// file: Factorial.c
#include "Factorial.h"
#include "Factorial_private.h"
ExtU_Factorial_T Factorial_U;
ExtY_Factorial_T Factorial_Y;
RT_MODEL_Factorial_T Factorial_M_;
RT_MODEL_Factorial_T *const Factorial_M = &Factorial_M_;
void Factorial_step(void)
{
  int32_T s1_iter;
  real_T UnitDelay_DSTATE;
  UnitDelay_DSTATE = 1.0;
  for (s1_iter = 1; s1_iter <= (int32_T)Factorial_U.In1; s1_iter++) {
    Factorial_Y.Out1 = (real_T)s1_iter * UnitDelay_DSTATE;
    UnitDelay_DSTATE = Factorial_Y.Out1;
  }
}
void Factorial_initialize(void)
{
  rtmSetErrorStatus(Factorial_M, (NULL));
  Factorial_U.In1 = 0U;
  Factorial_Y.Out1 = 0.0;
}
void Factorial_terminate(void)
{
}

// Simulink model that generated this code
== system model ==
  In1 : Inport
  Out1 : Outport  <- 1: Subsystem#1
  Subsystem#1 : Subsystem  <- 1: In1
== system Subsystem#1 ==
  Inport#1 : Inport
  ForIterator#1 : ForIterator  <- 1: Inport#1
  Outport#1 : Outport  <- 1: Product#1
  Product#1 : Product  <- 1: ForIterator#1, 2: UnitDelay
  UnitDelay : UnitDelay  InitialCondition=1  <- 1: Product#1
